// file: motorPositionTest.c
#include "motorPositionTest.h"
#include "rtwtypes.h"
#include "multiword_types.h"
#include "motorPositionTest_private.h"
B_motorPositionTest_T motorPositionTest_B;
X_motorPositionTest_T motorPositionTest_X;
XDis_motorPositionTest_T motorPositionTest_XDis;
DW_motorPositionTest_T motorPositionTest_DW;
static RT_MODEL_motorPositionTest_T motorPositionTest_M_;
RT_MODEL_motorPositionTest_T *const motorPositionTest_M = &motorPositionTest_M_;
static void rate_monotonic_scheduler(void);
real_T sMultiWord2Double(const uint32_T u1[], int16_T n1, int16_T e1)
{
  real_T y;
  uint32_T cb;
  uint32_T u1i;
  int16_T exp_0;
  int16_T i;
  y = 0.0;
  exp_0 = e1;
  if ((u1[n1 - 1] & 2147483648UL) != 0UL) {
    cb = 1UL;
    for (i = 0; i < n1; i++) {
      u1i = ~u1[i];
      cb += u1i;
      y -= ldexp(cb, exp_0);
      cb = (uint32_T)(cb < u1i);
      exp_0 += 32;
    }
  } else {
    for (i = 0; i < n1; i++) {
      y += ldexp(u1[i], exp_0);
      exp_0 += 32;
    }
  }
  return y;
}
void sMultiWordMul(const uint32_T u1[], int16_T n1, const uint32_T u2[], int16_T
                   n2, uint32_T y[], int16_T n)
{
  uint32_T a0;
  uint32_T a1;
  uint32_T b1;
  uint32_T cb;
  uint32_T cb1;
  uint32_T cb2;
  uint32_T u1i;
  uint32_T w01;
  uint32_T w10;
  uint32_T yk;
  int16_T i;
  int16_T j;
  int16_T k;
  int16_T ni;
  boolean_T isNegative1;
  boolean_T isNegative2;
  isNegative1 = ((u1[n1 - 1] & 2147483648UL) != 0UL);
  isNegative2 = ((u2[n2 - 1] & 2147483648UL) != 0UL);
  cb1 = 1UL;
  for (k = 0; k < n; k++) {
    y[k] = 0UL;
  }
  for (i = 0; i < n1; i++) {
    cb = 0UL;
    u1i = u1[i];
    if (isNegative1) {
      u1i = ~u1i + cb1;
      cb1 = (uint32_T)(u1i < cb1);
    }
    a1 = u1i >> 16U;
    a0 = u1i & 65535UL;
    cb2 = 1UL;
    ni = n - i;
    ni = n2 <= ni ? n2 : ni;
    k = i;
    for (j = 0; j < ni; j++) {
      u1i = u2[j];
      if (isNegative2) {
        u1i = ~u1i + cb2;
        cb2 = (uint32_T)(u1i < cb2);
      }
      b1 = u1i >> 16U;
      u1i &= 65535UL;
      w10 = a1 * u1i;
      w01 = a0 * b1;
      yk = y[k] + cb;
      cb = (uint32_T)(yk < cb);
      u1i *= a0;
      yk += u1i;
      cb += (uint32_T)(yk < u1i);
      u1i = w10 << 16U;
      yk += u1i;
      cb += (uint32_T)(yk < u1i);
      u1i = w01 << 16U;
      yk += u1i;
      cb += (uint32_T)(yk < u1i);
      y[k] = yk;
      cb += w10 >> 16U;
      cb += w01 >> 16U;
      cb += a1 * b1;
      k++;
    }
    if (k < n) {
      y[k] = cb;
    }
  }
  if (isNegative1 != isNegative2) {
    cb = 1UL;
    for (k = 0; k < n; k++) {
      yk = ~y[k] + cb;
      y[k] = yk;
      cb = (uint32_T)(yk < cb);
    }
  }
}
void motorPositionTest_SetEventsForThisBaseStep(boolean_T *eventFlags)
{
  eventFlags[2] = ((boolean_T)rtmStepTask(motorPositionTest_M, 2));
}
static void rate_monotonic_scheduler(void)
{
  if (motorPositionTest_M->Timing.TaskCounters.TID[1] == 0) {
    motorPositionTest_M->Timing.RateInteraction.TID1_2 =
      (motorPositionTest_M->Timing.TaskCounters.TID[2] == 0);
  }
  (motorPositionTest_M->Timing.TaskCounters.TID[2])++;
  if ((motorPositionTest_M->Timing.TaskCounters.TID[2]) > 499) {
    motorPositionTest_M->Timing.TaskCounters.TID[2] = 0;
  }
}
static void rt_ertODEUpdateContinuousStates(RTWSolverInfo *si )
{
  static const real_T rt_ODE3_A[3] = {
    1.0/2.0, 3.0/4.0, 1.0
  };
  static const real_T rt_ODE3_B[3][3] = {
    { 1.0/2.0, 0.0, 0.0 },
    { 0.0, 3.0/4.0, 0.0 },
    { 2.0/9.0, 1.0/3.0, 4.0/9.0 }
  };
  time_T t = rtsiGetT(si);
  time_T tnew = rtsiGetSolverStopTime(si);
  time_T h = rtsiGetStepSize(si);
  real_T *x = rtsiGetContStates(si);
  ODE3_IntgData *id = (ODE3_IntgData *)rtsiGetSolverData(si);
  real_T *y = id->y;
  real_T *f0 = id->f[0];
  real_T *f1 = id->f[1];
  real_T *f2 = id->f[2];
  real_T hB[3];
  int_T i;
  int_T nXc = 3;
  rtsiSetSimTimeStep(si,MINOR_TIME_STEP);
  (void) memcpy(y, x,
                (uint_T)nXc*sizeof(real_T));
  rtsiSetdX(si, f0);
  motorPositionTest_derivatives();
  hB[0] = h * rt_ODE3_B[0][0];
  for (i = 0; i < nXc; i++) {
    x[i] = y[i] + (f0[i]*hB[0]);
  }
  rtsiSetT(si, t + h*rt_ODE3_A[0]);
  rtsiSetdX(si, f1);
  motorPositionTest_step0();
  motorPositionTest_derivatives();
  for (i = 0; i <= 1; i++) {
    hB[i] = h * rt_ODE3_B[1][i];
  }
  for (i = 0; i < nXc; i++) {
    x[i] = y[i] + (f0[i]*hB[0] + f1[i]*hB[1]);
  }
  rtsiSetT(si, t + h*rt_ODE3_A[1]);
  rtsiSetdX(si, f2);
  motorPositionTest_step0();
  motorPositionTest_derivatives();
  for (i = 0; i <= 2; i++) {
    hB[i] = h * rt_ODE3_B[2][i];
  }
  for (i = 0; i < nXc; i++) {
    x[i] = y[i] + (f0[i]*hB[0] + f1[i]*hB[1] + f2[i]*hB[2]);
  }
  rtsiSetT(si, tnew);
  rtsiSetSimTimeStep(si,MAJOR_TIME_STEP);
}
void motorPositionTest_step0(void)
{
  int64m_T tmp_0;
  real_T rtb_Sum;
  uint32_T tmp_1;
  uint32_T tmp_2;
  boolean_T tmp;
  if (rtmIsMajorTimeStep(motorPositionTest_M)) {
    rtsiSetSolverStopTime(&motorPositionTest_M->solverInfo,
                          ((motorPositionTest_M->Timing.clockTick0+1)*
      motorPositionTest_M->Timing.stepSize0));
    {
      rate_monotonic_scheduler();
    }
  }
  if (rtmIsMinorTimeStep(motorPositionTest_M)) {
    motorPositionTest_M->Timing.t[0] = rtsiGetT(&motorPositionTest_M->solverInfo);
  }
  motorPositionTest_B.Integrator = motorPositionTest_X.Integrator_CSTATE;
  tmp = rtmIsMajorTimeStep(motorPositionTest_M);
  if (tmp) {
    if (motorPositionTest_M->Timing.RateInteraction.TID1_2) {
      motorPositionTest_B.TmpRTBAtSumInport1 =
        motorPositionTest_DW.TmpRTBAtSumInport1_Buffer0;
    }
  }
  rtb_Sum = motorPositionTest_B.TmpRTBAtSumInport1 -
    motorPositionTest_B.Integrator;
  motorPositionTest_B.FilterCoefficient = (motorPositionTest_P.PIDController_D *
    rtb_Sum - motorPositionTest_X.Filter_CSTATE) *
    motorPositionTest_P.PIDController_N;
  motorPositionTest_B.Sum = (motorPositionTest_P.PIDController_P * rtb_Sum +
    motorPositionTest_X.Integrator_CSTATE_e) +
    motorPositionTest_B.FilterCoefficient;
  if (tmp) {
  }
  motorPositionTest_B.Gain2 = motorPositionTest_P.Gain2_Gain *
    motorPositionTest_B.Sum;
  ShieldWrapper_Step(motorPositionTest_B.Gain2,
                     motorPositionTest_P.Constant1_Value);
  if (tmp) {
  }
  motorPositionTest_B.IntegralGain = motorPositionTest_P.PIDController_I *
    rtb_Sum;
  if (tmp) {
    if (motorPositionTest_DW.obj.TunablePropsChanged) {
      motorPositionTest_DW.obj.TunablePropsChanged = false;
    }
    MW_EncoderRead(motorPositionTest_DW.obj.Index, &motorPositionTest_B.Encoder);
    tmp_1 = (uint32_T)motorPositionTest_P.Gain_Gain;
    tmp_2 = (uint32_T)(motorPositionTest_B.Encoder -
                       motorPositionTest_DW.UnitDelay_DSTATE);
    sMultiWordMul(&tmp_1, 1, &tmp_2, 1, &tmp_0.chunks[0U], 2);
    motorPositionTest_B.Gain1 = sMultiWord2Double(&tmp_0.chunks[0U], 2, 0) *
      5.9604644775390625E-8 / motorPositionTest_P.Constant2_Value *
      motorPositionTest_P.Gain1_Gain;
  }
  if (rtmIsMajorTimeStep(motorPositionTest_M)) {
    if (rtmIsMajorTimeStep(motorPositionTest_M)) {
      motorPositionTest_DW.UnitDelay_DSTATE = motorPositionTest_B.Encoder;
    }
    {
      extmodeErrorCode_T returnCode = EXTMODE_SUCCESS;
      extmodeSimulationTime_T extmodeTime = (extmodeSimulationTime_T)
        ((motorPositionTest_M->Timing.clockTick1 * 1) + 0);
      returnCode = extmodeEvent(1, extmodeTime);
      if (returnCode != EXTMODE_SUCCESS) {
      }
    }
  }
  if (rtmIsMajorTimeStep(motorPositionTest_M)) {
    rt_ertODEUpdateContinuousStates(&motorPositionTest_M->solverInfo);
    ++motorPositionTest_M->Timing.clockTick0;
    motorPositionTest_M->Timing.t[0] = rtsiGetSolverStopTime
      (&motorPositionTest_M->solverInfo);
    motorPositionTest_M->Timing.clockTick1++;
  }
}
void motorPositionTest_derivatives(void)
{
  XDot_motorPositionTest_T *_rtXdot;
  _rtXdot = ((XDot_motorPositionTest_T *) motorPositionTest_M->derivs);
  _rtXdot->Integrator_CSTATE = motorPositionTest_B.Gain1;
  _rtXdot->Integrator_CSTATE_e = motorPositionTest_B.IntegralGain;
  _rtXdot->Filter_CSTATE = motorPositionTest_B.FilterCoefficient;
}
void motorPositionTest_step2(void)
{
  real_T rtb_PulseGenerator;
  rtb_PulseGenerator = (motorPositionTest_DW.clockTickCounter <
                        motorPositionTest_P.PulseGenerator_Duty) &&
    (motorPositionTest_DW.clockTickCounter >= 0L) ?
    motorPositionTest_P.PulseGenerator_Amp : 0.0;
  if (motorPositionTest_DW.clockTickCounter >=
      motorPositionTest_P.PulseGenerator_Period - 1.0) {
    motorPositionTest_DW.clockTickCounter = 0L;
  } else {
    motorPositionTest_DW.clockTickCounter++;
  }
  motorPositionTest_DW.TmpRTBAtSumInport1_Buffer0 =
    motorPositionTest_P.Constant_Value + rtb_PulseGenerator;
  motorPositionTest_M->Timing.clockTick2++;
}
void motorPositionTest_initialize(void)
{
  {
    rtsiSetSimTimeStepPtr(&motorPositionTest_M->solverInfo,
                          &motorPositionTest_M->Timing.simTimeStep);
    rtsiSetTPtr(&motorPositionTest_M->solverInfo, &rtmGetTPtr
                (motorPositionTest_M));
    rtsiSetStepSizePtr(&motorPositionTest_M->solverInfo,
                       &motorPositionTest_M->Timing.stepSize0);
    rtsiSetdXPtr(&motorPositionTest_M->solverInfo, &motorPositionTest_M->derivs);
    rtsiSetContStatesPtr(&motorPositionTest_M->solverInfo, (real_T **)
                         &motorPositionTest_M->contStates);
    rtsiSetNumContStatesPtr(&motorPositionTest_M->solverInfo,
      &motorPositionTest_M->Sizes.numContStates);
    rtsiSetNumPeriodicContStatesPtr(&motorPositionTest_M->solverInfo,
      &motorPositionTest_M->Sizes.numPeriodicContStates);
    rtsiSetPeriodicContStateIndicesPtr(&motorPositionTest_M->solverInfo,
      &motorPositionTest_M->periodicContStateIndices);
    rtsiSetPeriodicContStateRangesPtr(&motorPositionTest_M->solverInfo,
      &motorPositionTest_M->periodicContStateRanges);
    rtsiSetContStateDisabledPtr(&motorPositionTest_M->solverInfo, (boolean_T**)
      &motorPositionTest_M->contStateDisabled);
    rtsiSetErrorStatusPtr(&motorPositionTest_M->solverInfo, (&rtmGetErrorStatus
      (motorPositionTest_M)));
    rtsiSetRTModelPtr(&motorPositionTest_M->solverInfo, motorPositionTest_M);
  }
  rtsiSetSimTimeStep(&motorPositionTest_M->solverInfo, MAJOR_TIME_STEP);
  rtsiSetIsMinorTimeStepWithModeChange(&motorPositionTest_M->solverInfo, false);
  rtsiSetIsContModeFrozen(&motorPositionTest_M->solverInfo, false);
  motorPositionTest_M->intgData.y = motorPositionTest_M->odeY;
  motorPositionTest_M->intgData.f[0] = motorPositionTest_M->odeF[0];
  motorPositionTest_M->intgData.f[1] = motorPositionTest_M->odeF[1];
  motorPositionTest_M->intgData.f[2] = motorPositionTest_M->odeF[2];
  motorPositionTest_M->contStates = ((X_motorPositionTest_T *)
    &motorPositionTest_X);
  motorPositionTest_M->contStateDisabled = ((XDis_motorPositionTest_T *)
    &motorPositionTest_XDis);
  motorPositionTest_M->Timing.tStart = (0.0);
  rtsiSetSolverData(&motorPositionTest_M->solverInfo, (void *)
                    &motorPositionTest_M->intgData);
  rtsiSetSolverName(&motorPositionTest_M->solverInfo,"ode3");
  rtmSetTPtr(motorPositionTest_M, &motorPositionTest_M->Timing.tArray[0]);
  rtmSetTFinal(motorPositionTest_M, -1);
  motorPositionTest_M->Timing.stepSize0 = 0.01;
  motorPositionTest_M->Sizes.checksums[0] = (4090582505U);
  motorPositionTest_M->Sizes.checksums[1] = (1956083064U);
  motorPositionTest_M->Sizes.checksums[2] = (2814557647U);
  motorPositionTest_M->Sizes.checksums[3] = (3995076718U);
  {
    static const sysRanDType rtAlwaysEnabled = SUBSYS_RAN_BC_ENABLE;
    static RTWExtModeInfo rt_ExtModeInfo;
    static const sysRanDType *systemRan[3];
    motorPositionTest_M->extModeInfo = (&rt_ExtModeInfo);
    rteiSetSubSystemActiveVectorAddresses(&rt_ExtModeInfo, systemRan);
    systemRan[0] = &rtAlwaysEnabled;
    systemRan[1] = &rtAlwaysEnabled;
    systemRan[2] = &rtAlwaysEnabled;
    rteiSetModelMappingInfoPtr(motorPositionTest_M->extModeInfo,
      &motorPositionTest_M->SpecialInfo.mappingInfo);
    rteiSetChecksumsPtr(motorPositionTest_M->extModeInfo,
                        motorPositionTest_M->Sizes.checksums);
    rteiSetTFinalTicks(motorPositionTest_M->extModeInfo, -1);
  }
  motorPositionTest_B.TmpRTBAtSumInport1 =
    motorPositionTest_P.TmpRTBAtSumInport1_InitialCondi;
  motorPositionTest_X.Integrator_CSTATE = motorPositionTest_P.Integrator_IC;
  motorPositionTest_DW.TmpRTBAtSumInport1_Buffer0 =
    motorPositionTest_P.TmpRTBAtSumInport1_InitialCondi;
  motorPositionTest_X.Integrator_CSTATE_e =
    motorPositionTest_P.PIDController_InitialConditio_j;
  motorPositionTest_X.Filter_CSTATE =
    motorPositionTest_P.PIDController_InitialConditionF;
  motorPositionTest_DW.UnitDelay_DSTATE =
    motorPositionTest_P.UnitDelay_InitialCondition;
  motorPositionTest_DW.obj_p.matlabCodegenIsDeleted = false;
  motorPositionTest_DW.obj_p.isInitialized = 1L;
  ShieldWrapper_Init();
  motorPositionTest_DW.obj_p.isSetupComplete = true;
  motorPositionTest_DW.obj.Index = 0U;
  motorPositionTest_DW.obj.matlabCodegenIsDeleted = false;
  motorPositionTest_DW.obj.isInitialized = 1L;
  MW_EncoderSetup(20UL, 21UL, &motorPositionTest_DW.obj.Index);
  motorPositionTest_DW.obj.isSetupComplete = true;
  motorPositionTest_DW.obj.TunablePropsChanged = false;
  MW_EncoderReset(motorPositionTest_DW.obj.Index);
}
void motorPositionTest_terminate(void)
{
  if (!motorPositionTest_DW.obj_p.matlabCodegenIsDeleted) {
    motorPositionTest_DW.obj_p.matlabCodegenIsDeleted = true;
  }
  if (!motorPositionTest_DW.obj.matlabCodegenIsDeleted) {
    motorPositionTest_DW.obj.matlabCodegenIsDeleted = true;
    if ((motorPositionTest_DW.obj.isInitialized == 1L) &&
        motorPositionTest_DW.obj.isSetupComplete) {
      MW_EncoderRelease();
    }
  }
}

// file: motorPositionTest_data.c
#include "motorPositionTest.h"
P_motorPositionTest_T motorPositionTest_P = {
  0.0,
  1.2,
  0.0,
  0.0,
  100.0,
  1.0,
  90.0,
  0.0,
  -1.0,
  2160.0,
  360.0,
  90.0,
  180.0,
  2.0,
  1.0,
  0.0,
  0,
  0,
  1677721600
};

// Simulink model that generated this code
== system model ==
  MATLABSystem#1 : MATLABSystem  <- 1: Gain2, 2: Constant1
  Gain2 : Gain  Gain=-1  <- 1: PIDController
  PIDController : slpidlib/PID Controller  Controller=PID  Form=Parallel  TimeDomain=Continuous-time  IntegratorMethod=Forward Euler  P=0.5  I=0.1  D=0  N=100  InitialConditionForIntegrator=0  ExternalReset=none  LimitOutput=off  UpperSaturationLimit=inf  LowerSaturationLimit=-inf  <- 1: Sum
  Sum : Sum  Inputs=+-  <- 1: Sum#1, 2: Integrator
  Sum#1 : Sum  <- 1: Constant, 2: PulseGenerator
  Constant : Constant  Value=90
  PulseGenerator : DiscretePulseGenerator  Amplitude=180  Period=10  PulseWidth=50
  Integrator : Integrator  InitialCondition=90  <- 1: Gain1
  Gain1 : Gain  Gain=360  <- 1: Product#1
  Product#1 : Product  Inputs=*/  <- 1: Gain, 2: Constant2
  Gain : Gain  Gain=100  <- 1: Sum#2
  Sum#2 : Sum  Inputs=+-  <- 1: Encoder, 2: UnitDelay
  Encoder : arduinosensorlib/Encoder
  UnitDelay : UnitDelay  <- 1: Encoder
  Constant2 : Constant  Value=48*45
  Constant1 : Constant  Value=0
